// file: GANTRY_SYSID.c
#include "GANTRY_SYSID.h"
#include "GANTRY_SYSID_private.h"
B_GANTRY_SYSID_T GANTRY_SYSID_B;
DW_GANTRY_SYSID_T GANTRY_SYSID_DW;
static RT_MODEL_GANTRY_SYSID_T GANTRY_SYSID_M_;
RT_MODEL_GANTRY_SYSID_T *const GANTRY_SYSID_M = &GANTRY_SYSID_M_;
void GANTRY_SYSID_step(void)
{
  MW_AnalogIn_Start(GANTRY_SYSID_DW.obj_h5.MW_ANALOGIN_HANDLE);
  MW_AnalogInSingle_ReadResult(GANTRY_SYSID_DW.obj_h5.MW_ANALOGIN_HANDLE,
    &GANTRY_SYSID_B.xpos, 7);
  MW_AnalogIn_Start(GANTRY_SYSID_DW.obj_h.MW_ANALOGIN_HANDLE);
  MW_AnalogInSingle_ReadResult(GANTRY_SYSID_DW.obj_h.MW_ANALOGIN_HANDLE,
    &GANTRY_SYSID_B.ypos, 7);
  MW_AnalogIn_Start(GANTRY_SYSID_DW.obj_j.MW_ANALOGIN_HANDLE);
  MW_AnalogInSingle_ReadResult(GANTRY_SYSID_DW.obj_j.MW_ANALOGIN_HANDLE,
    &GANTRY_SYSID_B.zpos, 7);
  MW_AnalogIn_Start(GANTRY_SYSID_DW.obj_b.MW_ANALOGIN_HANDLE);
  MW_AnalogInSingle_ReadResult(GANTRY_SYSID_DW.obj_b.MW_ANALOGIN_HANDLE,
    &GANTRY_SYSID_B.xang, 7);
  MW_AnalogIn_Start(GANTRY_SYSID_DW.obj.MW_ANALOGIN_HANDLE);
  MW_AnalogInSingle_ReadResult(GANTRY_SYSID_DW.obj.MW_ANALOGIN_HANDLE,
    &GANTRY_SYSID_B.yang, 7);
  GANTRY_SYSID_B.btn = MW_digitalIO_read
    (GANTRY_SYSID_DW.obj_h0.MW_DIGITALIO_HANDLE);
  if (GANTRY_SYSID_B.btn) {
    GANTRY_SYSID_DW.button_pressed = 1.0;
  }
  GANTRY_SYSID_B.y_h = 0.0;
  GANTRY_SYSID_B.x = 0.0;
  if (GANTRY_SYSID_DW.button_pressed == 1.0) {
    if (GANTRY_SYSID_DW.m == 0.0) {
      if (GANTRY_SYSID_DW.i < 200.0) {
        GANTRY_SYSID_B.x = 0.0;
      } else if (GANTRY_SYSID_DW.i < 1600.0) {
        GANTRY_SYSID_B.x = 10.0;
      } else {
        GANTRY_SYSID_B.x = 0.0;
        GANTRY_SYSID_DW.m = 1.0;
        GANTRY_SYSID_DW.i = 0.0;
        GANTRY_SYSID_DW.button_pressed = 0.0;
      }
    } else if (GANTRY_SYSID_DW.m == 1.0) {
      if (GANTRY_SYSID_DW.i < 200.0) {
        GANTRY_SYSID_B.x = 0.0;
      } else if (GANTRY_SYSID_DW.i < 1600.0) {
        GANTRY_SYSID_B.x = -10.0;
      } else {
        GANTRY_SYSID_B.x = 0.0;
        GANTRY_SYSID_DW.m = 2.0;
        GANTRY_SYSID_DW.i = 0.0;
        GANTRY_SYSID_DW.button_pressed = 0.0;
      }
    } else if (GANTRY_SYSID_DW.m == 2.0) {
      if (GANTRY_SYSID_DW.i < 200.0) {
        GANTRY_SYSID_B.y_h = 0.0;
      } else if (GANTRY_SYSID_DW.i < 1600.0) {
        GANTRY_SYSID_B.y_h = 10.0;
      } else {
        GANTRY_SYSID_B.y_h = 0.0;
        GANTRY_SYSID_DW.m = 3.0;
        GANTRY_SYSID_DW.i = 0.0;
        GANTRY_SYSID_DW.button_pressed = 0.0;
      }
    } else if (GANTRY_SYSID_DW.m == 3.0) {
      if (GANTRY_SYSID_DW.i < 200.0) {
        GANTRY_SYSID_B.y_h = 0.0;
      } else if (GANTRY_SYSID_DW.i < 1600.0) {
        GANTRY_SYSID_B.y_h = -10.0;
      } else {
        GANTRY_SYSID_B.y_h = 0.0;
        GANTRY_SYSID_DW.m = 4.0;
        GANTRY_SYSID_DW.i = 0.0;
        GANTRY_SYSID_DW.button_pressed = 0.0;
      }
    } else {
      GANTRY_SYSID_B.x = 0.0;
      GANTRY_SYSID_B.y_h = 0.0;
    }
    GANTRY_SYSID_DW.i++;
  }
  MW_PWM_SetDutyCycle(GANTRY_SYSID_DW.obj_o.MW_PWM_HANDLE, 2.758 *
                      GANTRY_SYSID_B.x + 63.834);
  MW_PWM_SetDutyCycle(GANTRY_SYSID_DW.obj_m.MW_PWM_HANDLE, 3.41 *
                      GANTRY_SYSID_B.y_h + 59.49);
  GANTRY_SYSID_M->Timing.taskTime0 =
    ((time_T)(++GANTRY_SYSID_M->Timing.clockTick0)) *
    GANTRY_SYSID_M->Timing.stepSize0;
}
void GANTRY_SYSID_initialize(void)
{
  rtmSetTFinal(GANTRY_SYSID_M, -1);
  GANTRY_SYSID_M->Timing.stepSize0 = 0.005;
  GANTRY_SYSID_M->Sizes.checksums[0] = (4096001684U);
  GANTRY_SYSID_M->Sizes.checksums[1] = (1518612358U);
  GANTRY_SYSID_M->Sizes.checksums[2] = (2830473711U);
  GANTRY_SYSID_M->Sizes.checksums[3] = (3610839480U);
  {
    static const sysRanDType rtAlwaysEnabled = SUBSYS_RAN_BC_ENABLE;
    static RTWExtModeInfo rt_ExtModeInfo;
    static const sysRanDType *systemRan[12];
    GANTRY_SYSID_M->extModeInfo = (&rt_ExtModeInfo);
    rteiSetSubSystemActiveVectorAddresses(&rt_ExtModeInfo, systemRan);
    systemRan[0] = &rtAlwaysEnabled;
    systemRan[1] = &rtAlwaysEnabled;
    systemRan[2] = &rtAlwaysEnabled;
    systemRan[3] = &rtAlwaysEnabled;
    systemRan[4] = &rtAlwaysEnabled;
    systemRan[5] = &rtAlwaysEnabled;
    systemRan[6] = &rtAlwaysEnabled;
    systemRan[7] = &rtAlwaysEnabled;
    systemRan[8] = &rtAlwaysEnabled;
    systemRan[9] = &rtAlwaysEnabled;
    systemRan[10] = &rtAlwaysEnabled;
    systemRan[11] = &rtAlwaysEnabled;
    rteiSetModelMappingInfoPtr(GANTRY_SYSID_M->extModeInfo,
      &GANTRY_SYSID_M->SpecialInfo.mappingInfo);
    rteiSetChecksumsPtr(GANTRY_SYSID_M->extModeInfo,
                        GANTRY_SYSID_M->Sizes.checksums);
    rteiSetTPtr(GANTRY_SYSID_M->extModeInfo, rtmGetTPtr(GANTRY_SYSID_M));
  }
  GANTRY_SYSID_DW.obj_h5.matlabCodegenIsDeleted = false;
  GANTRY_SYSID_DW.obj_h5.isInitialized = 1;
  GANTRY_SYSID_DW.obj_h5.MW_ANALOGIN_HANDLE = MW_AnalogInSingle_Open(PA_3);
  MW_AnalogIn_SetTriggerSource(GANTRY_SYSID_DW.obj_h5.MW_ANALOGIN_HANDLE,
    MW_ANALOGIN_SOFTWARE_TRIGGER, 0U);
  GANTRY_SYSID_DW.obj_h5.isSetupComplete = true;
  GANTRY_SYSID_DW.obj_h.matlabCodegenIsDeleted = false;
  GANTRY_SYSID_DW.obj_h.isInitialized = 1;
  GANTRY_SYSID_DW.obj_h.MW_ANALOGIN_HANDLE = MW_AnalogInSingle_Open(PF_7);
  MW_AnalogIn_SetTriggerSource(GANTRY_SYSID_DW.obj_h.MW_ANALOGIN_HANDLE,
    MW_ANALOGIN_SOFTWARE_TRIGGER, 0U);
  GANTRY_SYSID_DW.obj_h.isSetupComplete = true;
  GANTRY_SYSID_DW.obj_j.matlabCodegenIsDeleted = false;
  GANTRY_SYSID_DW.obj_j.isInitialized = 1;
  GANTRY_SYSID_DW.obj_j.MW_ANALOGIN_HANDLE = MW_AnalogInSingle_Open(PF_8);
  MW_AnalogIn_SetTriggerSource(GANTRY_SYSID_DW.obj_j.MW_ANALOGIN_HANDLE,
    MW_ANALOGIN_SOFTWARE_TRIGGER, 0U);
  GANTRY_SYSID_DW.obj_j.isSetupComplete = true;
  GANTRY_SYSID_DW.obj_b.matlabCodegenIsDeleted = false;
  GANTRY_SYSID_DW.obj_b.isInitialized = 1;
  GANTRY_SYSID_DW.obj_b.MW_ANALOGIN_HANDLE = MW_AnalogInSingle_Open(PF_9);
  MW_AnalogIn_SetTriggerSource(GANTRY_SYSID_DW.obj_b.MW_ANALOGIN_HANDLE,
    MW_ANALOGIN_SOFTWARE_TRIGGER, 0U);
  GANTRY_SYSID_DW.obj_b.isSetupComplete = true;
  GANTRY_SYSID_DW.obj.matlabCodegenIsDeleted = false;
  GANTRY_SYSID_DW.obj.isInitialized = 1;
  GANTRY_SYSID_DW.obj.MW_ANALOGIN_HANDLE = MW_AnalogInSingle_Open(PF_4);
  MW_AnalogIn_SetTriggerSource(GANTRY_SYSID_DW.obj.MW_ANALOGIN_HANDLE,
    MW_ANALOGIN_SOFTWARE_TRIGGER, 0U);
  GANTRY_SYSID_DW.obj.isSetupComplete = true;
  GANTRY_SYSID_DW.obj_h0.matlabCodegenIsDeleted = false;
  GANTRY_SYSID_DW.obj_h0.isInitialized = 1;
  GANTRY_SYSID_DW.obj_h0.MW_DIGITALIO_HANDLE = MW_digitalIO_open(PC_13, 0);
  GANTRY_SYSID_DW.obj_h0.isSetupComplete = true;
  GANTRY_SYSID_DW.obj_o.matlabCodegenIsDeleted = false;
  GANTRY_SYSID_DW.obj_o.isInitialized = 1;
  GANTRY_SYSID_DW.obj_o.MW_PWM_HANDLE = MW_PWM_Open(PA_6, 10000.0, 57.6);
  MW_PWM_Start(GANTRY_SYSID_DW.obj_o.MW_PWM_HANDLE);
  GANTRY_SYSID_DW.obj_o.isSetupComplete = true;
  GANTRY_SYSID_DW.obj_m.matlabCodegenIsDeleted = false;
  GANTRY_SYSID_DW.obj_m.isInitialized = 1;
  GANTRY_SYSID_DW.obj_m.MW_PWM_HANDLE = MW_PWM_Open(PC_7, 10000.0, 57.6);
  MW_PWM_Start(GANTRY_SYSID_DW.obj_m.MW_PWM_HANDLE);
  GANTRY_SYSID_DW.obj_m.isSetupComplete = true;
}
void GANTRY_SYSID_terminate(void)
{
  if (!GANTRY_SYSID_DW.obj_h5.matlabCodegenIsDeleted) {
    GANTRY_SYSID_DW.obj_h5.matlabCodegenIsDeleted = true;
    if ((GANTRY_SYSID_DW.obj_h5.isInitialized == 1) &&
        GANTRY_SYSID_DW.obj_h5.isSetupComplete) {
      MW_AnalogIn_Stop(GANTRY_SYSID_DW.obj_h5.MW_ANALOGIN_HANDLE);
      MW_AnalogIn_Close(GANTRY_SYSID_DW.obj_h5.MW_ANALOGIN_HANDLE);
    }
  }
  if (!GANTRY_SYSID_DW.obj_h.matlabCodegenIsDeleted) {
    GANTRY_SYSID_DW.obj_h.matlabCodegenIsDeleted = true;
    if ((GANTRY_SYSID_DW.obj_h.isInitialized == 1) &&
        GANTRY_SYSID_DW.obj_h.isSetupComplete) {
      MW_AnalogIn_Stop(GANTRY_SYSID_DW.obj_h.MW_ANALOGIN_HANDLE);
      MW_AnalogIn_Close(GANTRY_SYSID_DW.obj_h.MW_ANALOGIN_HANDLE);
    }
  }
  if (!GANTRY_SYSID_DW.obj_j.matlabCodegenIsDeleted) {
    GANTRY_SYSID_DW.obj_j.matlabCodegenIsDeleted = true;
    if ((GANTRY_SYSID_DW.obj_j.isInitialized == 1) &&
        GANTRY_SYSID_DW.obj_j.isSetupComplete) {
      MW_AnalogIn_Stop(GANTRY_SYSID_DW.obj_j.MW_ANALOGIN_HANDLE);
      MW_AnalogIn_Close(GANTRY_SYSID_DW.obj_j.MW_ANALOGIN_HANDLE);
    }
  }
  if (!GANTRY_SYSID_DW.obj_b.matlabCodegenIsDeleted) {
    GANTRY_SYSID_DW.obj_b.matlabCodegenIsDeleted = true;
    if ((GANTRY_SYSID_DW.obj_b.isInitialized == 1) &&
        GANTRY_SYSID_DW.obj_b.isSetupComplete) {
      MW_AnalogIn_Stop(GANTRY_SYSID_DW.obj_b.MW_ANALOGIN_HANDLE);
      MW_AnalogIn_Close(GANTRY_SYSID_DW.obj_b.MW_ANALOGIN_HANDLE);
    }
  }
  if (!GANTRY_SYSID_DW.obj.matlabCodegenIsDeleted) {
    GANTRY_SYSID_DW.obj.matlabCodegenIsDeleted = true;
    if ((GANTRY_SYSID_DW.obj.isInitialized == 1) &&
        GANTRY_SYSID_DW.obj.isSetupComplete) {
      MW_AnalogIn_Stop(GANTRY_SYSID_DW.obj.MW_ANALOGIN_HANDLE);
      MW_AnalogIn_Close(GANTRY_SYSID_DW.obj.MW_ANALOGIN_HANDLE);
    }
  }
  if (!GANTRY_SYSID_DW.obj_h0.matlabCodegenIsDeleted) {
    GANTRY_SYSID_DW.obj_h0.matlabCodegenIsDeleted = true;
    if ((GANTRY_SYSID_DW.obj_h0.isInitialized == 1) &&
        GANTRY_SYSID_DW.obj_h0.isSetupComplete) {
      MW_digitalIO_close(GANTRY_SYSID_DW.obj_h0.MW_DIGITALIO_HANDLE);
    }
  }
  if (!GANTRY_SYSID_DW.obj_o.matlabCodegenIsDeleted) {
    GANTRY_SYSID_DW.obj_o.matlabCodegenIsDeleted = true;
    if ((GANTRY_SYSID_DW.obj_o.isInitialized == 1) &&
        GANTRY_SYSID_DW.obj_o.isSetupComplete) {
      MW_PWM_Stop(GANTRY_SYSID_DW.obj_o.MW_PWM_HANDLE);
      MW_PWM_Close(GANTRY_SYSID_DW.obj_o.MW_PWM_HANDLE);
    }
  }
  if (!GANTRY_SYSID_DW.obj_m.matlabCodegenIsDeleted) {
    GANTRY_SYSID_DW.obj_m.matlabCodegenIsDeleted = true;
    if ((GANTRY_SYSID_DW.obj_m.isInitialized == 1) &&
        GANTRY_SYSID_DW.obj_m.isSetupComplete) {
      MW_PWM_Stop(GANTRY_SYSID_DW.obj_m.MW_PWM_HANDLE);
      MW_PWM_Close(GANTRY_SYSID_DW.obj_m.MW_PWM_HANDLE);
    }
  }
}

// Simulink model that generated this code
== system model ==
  AnalogInput#1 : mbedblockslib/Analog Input
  AnalogInput#2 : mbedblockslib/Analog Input
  AnalogInput#3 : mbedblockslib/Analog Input
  AnalogInput#4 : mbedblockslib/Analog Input
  AnalogInput#5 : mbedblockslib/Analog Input
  PWMOutput#1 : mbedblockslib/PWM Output  <- 1: MATLABFunction#1
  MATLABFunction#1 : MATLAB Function  <- 1: MATLABFunction#2/2
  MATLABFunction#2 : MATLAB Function  <- 1: DigitalRead#1
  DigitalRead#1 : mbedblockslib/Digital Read
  PWMOutput#2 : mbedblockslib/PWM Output  <- 1: MATLABFunction#3
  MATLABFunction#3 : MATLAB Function  <- 1: MATLABFunction#2
== matlab function MATLABFunction#2 ==
function [y, x]= fcn(user_button)

persistent i m button_pressed

if isempty(m)
    m = 0;
    i = 0;
    button_pressed = 0;
end

Fs = 200;

if user_button == 1
    button_pressed = 1;
end

y = 0;
x = 0;
if button_pressed == 1
    if m == 0
        if i < 1*Fs
            x = 0;
        elseif i < 8*Fs
            x = 10;
        else
            x = 0;
            m = 1;
            i = 0;
            button_pressed = 0;
        end
    elseif m == 1
        if i < 1*Fs
            x = 0;
        elseif i < 8*Fs
            x = -10;
        else
            x = 0;
            m = 2;
            i = 0;
            button_pressed = 0;
        end
    elseif m == 2
        if i < 1*Fs
            y = 0;
        elseif i < 8*Fs
            y = 10;
        else
            y = 0;
            m = 3;
            i = 0;
            button_pressed = 0;
        end
    elseif m == 3
        if i < 1*Fs
            y = 0;
        elseif i < 8*Fs
            y = -10;
        else
            y = 0;
            m = 4;
            i = 0;
            button_pressed = 0;
        end
    else
        % Do Nothing
        x = 0;
        y = 0;
    end

    i = i + 1;
end

end

== matlab function MATLABFunction#3 ==
function y = fcn(u)

y = 3.41*u + 59.49;

== matlab function MATLABFunction#1 ==
function y = fcn(u)

y = 2.758*u + 63.834;
